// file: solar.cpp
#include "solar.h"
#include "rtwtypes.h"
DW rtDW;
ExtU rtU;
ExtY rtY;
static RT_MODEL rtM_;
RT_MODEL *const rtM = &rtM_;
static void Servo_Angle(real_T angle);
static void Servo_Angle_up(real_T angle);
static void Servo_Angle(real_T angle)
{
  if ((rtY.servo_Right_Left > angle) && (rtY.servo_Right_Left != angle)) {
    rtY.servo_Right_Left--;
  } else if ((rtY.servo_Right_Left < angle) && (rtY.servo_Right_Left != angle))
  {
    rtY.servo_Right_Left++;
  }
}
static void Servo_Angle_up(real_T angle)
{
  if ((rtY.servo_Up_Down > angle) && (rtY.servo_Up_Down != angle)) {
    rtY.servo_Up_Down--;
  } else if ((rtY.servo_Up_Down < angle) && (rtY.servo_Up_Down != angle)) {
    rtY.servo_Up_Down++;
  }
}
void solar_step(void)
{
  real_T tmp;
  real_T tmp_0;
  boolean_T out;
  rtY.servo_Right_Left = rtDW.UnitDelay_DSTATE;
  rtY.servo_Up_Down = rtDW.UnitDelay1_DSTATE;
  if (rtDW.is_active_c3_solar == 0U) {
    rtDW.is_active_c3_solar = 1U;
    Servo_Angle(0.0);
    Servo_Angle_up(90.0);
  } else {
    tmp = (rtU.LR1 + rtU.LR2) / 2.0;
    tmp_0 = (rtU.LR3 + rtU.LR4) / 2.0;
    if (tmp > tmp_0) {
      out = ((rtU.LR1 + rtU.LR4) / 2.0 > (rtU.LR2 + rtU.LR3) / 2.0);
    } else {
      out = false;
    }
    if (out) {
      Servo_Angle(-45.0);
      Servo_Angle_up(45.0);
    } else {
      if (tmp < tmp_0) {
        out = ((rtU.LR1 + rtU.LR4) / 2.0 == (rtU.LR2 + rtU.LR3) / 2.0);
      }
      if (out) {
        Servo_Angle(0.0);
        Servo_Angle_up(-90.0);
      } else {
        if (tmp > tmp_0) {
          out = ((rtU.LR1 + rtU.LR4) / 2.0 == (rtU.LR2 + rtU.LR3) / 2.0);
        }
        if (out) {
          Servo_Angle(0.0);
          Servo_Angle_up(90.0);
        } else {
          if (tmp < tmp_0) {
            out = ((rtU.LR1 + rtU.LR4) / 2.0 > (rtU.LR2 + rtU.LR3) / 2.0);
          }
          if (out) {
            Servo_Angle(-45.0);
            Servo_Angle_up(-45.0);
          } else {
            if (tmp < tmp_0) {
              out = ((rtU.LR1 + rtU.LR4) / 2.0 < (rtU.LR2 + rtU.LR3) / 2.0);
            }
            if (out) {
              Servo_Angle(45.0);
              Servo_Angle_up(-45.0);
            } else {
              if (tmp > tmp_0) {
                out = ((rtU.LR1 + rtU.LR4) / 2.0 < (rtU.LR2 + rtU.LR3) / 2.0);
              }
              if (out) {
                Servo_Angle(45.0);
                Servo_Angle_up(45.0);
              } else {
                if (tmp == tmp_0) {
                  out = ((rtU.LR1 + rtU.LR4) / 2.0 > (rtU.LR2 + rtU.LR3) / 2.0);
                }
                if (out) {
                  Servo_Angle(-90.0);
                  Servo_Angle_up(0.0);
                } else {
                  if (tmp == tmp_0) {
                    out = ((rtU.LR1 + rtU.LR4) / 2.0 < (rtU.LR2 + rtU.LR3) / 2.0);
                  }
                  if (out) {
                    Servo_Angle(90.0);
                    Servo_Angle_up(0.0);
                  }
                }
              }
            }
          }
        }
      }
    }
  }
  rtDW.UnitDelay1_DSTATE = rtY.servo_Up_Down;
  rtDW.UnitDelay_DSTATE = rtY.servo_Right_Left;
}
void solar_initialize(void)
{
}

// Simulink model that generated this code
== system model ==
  LR1 : Inport
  LR2 : Inport
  LR3 : Inport
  LR4 : Inport
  servo_Right_Left : Outport  <- 1: Stateflowchart#1
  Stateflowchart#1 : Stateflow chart  <- 1: LR1, 2: UnitDelay1, 3: UnitDelay, 4: LR2, 5: LR3, 6: LR4
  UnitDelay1 : UnitDelay  <- 1: Stateflowchart#1/2
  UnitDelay : UnitDelay  <- 1: Stateflowchart#1
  servo_Up_Down : Outport  <- 1: Stateflowchart#1/2
== stateflow chart Stateflowchart#1 ==
  state mode
    state mode_up
      (default) -> (junction 205) : {Servo_Angle(0);}
      (junction 205) -> (junction 204) : {Servo_Angle_up(90);}
    state mode_down
      (default) -> (junction 173) : {Servo_Angle(0);}
      (junction 173) -> (junction 198) : {Servo_Angle_up(-90);}
    state mode_Right
      (default) -> (junction 209) : {Servo_Angle(90);}
      (junction 209) -> (junction 208) : {Servo_Angle_up(0);}
    state mode_Left
      (default) -> (junction 213) : {Servo_Angle(-90);}
      (junction 213) -> (junction 212) : {Servo_Angle_up(0);}
    state mode_Right_Up
      (default) -> (junction 218) : {Servo_Angle(45);}
      (junction 218) -> (junction 217) : {Servo_Angle_up(45);}
    state mode_Right_Down
      (default) -> (junction 222) : {Servo_Angle(45);}
      (junction 222) -> (junction 221) : {Servo_Angle_up(-45);}
    state mode_Left_Down
      (default) -> (junction 228) : {Servo_Angle(-45);}
      (junction 228) -> (junction 227) : {Servo_Angle_up(-45);}
    state mode_Left_Up
      (default) -> (junction 232) : {Servo_Angle(-45);}
      (junction 232) -> (junction 231) : {Servo_Angle_up(45);}
    (default) -> mode_up
    mode -> mode_up [order 3] : [((LR1+LR2 )/2 >(LR3+LR4)/2) &&((LR1+LR4)/2 == (LR2+LR3)/2)]
    mode -> mode_down [order 2] : [((LR1+LR2 )/2 <(LR3+LR4)/2) &&((LR1+LR4)/2 == (LR2+LR3)/2)]
    mode -> mode_Right [order 8] : [((LR1+LR2 )/2 == (LR3+LR4)/2) &&((LR1+LR4)/2 < (LR2+LR3)/2)]
    mode -> mode_Left [order 7] : [((LR1+LR2 )/2 == (LR3+LR4)/2) &&((LR1+LR4)/2 > (LR2+LR3)/2)]
    mode -> mode_Right_Up [order 6] : [((LR1+LR2 )/2 >(LR3+LR4)/2) &&((LR1+LR4)/2 < (LR2+LR3)/2)]
    mode -> mode_Right_Down [order 5] : [((LR1+LR2 )/2  < (LR3+LR4)/2) &&((LR1+LR4)/2 < (LR2+LR3)/2)]
    mode -> mode_Left_Down [order 4] : [((LR1+LR2 )/2  < (LR3+LR4)/2) &&((LR1+LR4)/2 > (LR2+LR3)/2)]
    mode -> mode_Left_Up [order 1] : [((LR1+LR2 )/2 >(LR3+LR4)/2) &&((LR1+LR4)/2 > (LR2+LR3)/2)]
  state Servo_Angle_up(angle) [function]
    (default) -> (junction 181)
    (junction 181) -> (junction 184)
    (junction 184) -> (junction 186) [order 1] : [(servo_Up_Down >angle) && (servo_Up_Down~=angle)]
    (junction 184) -> (junction 175) [order 2]
    (junction 186) -> (junction 190) : {servo_Up_Down = servo_Up_Down - 1;}
    (junction 175) -> (junction 189) [order 1] : [(servo_Up_Down <angle) && (servo_Up_Down~=angle) ]
    (junction 175) -> (junction 191) [order 2]
    (junction 189) -> (junction 192) : {servo_Up_Down = servo_Up_Down + 1;}
    (junction 192) -> (junction 191)
    (junction 190) -> (junction 192)
    (junction 191) -> (junction 180)
  state Servo_Angle(angle) [function]
    (default) -> (junction 150)
    (junction 150) -> (junction 164)
    (junction 164) -> (junction 165) [order 1] : [(servo_Right_Left >angle) && (servo_Right_Left~=angle) ]
    (junction 164) -> (junction 166) [order 2]
    (junction 165) -> (junction 170) : {servo_Right_Left = servo_Right_Left - 1;}
    (junction 166) -> (junction 167) [order 1] : [(servo_Right_Left <angle) && (servo_Right_Left~=angle) ]
    (junction 166) -> (junction 168) [order 2]
    (junction 167) -> (junction 169) : {servo_Right_Left = servo_Right_Left + 1;}
    (junction 169) -> (junction 168)
    (junction 170) -> (junction 169)
    (junction 168) -> (junction 171)
  data: angle function_input; angle function_input; LR1 input; servo_Up_Down input; servo_Right_Left input; LR2 input; LR3 input; LR4 input; servo_Right_Left output; servo_Up_Down output
